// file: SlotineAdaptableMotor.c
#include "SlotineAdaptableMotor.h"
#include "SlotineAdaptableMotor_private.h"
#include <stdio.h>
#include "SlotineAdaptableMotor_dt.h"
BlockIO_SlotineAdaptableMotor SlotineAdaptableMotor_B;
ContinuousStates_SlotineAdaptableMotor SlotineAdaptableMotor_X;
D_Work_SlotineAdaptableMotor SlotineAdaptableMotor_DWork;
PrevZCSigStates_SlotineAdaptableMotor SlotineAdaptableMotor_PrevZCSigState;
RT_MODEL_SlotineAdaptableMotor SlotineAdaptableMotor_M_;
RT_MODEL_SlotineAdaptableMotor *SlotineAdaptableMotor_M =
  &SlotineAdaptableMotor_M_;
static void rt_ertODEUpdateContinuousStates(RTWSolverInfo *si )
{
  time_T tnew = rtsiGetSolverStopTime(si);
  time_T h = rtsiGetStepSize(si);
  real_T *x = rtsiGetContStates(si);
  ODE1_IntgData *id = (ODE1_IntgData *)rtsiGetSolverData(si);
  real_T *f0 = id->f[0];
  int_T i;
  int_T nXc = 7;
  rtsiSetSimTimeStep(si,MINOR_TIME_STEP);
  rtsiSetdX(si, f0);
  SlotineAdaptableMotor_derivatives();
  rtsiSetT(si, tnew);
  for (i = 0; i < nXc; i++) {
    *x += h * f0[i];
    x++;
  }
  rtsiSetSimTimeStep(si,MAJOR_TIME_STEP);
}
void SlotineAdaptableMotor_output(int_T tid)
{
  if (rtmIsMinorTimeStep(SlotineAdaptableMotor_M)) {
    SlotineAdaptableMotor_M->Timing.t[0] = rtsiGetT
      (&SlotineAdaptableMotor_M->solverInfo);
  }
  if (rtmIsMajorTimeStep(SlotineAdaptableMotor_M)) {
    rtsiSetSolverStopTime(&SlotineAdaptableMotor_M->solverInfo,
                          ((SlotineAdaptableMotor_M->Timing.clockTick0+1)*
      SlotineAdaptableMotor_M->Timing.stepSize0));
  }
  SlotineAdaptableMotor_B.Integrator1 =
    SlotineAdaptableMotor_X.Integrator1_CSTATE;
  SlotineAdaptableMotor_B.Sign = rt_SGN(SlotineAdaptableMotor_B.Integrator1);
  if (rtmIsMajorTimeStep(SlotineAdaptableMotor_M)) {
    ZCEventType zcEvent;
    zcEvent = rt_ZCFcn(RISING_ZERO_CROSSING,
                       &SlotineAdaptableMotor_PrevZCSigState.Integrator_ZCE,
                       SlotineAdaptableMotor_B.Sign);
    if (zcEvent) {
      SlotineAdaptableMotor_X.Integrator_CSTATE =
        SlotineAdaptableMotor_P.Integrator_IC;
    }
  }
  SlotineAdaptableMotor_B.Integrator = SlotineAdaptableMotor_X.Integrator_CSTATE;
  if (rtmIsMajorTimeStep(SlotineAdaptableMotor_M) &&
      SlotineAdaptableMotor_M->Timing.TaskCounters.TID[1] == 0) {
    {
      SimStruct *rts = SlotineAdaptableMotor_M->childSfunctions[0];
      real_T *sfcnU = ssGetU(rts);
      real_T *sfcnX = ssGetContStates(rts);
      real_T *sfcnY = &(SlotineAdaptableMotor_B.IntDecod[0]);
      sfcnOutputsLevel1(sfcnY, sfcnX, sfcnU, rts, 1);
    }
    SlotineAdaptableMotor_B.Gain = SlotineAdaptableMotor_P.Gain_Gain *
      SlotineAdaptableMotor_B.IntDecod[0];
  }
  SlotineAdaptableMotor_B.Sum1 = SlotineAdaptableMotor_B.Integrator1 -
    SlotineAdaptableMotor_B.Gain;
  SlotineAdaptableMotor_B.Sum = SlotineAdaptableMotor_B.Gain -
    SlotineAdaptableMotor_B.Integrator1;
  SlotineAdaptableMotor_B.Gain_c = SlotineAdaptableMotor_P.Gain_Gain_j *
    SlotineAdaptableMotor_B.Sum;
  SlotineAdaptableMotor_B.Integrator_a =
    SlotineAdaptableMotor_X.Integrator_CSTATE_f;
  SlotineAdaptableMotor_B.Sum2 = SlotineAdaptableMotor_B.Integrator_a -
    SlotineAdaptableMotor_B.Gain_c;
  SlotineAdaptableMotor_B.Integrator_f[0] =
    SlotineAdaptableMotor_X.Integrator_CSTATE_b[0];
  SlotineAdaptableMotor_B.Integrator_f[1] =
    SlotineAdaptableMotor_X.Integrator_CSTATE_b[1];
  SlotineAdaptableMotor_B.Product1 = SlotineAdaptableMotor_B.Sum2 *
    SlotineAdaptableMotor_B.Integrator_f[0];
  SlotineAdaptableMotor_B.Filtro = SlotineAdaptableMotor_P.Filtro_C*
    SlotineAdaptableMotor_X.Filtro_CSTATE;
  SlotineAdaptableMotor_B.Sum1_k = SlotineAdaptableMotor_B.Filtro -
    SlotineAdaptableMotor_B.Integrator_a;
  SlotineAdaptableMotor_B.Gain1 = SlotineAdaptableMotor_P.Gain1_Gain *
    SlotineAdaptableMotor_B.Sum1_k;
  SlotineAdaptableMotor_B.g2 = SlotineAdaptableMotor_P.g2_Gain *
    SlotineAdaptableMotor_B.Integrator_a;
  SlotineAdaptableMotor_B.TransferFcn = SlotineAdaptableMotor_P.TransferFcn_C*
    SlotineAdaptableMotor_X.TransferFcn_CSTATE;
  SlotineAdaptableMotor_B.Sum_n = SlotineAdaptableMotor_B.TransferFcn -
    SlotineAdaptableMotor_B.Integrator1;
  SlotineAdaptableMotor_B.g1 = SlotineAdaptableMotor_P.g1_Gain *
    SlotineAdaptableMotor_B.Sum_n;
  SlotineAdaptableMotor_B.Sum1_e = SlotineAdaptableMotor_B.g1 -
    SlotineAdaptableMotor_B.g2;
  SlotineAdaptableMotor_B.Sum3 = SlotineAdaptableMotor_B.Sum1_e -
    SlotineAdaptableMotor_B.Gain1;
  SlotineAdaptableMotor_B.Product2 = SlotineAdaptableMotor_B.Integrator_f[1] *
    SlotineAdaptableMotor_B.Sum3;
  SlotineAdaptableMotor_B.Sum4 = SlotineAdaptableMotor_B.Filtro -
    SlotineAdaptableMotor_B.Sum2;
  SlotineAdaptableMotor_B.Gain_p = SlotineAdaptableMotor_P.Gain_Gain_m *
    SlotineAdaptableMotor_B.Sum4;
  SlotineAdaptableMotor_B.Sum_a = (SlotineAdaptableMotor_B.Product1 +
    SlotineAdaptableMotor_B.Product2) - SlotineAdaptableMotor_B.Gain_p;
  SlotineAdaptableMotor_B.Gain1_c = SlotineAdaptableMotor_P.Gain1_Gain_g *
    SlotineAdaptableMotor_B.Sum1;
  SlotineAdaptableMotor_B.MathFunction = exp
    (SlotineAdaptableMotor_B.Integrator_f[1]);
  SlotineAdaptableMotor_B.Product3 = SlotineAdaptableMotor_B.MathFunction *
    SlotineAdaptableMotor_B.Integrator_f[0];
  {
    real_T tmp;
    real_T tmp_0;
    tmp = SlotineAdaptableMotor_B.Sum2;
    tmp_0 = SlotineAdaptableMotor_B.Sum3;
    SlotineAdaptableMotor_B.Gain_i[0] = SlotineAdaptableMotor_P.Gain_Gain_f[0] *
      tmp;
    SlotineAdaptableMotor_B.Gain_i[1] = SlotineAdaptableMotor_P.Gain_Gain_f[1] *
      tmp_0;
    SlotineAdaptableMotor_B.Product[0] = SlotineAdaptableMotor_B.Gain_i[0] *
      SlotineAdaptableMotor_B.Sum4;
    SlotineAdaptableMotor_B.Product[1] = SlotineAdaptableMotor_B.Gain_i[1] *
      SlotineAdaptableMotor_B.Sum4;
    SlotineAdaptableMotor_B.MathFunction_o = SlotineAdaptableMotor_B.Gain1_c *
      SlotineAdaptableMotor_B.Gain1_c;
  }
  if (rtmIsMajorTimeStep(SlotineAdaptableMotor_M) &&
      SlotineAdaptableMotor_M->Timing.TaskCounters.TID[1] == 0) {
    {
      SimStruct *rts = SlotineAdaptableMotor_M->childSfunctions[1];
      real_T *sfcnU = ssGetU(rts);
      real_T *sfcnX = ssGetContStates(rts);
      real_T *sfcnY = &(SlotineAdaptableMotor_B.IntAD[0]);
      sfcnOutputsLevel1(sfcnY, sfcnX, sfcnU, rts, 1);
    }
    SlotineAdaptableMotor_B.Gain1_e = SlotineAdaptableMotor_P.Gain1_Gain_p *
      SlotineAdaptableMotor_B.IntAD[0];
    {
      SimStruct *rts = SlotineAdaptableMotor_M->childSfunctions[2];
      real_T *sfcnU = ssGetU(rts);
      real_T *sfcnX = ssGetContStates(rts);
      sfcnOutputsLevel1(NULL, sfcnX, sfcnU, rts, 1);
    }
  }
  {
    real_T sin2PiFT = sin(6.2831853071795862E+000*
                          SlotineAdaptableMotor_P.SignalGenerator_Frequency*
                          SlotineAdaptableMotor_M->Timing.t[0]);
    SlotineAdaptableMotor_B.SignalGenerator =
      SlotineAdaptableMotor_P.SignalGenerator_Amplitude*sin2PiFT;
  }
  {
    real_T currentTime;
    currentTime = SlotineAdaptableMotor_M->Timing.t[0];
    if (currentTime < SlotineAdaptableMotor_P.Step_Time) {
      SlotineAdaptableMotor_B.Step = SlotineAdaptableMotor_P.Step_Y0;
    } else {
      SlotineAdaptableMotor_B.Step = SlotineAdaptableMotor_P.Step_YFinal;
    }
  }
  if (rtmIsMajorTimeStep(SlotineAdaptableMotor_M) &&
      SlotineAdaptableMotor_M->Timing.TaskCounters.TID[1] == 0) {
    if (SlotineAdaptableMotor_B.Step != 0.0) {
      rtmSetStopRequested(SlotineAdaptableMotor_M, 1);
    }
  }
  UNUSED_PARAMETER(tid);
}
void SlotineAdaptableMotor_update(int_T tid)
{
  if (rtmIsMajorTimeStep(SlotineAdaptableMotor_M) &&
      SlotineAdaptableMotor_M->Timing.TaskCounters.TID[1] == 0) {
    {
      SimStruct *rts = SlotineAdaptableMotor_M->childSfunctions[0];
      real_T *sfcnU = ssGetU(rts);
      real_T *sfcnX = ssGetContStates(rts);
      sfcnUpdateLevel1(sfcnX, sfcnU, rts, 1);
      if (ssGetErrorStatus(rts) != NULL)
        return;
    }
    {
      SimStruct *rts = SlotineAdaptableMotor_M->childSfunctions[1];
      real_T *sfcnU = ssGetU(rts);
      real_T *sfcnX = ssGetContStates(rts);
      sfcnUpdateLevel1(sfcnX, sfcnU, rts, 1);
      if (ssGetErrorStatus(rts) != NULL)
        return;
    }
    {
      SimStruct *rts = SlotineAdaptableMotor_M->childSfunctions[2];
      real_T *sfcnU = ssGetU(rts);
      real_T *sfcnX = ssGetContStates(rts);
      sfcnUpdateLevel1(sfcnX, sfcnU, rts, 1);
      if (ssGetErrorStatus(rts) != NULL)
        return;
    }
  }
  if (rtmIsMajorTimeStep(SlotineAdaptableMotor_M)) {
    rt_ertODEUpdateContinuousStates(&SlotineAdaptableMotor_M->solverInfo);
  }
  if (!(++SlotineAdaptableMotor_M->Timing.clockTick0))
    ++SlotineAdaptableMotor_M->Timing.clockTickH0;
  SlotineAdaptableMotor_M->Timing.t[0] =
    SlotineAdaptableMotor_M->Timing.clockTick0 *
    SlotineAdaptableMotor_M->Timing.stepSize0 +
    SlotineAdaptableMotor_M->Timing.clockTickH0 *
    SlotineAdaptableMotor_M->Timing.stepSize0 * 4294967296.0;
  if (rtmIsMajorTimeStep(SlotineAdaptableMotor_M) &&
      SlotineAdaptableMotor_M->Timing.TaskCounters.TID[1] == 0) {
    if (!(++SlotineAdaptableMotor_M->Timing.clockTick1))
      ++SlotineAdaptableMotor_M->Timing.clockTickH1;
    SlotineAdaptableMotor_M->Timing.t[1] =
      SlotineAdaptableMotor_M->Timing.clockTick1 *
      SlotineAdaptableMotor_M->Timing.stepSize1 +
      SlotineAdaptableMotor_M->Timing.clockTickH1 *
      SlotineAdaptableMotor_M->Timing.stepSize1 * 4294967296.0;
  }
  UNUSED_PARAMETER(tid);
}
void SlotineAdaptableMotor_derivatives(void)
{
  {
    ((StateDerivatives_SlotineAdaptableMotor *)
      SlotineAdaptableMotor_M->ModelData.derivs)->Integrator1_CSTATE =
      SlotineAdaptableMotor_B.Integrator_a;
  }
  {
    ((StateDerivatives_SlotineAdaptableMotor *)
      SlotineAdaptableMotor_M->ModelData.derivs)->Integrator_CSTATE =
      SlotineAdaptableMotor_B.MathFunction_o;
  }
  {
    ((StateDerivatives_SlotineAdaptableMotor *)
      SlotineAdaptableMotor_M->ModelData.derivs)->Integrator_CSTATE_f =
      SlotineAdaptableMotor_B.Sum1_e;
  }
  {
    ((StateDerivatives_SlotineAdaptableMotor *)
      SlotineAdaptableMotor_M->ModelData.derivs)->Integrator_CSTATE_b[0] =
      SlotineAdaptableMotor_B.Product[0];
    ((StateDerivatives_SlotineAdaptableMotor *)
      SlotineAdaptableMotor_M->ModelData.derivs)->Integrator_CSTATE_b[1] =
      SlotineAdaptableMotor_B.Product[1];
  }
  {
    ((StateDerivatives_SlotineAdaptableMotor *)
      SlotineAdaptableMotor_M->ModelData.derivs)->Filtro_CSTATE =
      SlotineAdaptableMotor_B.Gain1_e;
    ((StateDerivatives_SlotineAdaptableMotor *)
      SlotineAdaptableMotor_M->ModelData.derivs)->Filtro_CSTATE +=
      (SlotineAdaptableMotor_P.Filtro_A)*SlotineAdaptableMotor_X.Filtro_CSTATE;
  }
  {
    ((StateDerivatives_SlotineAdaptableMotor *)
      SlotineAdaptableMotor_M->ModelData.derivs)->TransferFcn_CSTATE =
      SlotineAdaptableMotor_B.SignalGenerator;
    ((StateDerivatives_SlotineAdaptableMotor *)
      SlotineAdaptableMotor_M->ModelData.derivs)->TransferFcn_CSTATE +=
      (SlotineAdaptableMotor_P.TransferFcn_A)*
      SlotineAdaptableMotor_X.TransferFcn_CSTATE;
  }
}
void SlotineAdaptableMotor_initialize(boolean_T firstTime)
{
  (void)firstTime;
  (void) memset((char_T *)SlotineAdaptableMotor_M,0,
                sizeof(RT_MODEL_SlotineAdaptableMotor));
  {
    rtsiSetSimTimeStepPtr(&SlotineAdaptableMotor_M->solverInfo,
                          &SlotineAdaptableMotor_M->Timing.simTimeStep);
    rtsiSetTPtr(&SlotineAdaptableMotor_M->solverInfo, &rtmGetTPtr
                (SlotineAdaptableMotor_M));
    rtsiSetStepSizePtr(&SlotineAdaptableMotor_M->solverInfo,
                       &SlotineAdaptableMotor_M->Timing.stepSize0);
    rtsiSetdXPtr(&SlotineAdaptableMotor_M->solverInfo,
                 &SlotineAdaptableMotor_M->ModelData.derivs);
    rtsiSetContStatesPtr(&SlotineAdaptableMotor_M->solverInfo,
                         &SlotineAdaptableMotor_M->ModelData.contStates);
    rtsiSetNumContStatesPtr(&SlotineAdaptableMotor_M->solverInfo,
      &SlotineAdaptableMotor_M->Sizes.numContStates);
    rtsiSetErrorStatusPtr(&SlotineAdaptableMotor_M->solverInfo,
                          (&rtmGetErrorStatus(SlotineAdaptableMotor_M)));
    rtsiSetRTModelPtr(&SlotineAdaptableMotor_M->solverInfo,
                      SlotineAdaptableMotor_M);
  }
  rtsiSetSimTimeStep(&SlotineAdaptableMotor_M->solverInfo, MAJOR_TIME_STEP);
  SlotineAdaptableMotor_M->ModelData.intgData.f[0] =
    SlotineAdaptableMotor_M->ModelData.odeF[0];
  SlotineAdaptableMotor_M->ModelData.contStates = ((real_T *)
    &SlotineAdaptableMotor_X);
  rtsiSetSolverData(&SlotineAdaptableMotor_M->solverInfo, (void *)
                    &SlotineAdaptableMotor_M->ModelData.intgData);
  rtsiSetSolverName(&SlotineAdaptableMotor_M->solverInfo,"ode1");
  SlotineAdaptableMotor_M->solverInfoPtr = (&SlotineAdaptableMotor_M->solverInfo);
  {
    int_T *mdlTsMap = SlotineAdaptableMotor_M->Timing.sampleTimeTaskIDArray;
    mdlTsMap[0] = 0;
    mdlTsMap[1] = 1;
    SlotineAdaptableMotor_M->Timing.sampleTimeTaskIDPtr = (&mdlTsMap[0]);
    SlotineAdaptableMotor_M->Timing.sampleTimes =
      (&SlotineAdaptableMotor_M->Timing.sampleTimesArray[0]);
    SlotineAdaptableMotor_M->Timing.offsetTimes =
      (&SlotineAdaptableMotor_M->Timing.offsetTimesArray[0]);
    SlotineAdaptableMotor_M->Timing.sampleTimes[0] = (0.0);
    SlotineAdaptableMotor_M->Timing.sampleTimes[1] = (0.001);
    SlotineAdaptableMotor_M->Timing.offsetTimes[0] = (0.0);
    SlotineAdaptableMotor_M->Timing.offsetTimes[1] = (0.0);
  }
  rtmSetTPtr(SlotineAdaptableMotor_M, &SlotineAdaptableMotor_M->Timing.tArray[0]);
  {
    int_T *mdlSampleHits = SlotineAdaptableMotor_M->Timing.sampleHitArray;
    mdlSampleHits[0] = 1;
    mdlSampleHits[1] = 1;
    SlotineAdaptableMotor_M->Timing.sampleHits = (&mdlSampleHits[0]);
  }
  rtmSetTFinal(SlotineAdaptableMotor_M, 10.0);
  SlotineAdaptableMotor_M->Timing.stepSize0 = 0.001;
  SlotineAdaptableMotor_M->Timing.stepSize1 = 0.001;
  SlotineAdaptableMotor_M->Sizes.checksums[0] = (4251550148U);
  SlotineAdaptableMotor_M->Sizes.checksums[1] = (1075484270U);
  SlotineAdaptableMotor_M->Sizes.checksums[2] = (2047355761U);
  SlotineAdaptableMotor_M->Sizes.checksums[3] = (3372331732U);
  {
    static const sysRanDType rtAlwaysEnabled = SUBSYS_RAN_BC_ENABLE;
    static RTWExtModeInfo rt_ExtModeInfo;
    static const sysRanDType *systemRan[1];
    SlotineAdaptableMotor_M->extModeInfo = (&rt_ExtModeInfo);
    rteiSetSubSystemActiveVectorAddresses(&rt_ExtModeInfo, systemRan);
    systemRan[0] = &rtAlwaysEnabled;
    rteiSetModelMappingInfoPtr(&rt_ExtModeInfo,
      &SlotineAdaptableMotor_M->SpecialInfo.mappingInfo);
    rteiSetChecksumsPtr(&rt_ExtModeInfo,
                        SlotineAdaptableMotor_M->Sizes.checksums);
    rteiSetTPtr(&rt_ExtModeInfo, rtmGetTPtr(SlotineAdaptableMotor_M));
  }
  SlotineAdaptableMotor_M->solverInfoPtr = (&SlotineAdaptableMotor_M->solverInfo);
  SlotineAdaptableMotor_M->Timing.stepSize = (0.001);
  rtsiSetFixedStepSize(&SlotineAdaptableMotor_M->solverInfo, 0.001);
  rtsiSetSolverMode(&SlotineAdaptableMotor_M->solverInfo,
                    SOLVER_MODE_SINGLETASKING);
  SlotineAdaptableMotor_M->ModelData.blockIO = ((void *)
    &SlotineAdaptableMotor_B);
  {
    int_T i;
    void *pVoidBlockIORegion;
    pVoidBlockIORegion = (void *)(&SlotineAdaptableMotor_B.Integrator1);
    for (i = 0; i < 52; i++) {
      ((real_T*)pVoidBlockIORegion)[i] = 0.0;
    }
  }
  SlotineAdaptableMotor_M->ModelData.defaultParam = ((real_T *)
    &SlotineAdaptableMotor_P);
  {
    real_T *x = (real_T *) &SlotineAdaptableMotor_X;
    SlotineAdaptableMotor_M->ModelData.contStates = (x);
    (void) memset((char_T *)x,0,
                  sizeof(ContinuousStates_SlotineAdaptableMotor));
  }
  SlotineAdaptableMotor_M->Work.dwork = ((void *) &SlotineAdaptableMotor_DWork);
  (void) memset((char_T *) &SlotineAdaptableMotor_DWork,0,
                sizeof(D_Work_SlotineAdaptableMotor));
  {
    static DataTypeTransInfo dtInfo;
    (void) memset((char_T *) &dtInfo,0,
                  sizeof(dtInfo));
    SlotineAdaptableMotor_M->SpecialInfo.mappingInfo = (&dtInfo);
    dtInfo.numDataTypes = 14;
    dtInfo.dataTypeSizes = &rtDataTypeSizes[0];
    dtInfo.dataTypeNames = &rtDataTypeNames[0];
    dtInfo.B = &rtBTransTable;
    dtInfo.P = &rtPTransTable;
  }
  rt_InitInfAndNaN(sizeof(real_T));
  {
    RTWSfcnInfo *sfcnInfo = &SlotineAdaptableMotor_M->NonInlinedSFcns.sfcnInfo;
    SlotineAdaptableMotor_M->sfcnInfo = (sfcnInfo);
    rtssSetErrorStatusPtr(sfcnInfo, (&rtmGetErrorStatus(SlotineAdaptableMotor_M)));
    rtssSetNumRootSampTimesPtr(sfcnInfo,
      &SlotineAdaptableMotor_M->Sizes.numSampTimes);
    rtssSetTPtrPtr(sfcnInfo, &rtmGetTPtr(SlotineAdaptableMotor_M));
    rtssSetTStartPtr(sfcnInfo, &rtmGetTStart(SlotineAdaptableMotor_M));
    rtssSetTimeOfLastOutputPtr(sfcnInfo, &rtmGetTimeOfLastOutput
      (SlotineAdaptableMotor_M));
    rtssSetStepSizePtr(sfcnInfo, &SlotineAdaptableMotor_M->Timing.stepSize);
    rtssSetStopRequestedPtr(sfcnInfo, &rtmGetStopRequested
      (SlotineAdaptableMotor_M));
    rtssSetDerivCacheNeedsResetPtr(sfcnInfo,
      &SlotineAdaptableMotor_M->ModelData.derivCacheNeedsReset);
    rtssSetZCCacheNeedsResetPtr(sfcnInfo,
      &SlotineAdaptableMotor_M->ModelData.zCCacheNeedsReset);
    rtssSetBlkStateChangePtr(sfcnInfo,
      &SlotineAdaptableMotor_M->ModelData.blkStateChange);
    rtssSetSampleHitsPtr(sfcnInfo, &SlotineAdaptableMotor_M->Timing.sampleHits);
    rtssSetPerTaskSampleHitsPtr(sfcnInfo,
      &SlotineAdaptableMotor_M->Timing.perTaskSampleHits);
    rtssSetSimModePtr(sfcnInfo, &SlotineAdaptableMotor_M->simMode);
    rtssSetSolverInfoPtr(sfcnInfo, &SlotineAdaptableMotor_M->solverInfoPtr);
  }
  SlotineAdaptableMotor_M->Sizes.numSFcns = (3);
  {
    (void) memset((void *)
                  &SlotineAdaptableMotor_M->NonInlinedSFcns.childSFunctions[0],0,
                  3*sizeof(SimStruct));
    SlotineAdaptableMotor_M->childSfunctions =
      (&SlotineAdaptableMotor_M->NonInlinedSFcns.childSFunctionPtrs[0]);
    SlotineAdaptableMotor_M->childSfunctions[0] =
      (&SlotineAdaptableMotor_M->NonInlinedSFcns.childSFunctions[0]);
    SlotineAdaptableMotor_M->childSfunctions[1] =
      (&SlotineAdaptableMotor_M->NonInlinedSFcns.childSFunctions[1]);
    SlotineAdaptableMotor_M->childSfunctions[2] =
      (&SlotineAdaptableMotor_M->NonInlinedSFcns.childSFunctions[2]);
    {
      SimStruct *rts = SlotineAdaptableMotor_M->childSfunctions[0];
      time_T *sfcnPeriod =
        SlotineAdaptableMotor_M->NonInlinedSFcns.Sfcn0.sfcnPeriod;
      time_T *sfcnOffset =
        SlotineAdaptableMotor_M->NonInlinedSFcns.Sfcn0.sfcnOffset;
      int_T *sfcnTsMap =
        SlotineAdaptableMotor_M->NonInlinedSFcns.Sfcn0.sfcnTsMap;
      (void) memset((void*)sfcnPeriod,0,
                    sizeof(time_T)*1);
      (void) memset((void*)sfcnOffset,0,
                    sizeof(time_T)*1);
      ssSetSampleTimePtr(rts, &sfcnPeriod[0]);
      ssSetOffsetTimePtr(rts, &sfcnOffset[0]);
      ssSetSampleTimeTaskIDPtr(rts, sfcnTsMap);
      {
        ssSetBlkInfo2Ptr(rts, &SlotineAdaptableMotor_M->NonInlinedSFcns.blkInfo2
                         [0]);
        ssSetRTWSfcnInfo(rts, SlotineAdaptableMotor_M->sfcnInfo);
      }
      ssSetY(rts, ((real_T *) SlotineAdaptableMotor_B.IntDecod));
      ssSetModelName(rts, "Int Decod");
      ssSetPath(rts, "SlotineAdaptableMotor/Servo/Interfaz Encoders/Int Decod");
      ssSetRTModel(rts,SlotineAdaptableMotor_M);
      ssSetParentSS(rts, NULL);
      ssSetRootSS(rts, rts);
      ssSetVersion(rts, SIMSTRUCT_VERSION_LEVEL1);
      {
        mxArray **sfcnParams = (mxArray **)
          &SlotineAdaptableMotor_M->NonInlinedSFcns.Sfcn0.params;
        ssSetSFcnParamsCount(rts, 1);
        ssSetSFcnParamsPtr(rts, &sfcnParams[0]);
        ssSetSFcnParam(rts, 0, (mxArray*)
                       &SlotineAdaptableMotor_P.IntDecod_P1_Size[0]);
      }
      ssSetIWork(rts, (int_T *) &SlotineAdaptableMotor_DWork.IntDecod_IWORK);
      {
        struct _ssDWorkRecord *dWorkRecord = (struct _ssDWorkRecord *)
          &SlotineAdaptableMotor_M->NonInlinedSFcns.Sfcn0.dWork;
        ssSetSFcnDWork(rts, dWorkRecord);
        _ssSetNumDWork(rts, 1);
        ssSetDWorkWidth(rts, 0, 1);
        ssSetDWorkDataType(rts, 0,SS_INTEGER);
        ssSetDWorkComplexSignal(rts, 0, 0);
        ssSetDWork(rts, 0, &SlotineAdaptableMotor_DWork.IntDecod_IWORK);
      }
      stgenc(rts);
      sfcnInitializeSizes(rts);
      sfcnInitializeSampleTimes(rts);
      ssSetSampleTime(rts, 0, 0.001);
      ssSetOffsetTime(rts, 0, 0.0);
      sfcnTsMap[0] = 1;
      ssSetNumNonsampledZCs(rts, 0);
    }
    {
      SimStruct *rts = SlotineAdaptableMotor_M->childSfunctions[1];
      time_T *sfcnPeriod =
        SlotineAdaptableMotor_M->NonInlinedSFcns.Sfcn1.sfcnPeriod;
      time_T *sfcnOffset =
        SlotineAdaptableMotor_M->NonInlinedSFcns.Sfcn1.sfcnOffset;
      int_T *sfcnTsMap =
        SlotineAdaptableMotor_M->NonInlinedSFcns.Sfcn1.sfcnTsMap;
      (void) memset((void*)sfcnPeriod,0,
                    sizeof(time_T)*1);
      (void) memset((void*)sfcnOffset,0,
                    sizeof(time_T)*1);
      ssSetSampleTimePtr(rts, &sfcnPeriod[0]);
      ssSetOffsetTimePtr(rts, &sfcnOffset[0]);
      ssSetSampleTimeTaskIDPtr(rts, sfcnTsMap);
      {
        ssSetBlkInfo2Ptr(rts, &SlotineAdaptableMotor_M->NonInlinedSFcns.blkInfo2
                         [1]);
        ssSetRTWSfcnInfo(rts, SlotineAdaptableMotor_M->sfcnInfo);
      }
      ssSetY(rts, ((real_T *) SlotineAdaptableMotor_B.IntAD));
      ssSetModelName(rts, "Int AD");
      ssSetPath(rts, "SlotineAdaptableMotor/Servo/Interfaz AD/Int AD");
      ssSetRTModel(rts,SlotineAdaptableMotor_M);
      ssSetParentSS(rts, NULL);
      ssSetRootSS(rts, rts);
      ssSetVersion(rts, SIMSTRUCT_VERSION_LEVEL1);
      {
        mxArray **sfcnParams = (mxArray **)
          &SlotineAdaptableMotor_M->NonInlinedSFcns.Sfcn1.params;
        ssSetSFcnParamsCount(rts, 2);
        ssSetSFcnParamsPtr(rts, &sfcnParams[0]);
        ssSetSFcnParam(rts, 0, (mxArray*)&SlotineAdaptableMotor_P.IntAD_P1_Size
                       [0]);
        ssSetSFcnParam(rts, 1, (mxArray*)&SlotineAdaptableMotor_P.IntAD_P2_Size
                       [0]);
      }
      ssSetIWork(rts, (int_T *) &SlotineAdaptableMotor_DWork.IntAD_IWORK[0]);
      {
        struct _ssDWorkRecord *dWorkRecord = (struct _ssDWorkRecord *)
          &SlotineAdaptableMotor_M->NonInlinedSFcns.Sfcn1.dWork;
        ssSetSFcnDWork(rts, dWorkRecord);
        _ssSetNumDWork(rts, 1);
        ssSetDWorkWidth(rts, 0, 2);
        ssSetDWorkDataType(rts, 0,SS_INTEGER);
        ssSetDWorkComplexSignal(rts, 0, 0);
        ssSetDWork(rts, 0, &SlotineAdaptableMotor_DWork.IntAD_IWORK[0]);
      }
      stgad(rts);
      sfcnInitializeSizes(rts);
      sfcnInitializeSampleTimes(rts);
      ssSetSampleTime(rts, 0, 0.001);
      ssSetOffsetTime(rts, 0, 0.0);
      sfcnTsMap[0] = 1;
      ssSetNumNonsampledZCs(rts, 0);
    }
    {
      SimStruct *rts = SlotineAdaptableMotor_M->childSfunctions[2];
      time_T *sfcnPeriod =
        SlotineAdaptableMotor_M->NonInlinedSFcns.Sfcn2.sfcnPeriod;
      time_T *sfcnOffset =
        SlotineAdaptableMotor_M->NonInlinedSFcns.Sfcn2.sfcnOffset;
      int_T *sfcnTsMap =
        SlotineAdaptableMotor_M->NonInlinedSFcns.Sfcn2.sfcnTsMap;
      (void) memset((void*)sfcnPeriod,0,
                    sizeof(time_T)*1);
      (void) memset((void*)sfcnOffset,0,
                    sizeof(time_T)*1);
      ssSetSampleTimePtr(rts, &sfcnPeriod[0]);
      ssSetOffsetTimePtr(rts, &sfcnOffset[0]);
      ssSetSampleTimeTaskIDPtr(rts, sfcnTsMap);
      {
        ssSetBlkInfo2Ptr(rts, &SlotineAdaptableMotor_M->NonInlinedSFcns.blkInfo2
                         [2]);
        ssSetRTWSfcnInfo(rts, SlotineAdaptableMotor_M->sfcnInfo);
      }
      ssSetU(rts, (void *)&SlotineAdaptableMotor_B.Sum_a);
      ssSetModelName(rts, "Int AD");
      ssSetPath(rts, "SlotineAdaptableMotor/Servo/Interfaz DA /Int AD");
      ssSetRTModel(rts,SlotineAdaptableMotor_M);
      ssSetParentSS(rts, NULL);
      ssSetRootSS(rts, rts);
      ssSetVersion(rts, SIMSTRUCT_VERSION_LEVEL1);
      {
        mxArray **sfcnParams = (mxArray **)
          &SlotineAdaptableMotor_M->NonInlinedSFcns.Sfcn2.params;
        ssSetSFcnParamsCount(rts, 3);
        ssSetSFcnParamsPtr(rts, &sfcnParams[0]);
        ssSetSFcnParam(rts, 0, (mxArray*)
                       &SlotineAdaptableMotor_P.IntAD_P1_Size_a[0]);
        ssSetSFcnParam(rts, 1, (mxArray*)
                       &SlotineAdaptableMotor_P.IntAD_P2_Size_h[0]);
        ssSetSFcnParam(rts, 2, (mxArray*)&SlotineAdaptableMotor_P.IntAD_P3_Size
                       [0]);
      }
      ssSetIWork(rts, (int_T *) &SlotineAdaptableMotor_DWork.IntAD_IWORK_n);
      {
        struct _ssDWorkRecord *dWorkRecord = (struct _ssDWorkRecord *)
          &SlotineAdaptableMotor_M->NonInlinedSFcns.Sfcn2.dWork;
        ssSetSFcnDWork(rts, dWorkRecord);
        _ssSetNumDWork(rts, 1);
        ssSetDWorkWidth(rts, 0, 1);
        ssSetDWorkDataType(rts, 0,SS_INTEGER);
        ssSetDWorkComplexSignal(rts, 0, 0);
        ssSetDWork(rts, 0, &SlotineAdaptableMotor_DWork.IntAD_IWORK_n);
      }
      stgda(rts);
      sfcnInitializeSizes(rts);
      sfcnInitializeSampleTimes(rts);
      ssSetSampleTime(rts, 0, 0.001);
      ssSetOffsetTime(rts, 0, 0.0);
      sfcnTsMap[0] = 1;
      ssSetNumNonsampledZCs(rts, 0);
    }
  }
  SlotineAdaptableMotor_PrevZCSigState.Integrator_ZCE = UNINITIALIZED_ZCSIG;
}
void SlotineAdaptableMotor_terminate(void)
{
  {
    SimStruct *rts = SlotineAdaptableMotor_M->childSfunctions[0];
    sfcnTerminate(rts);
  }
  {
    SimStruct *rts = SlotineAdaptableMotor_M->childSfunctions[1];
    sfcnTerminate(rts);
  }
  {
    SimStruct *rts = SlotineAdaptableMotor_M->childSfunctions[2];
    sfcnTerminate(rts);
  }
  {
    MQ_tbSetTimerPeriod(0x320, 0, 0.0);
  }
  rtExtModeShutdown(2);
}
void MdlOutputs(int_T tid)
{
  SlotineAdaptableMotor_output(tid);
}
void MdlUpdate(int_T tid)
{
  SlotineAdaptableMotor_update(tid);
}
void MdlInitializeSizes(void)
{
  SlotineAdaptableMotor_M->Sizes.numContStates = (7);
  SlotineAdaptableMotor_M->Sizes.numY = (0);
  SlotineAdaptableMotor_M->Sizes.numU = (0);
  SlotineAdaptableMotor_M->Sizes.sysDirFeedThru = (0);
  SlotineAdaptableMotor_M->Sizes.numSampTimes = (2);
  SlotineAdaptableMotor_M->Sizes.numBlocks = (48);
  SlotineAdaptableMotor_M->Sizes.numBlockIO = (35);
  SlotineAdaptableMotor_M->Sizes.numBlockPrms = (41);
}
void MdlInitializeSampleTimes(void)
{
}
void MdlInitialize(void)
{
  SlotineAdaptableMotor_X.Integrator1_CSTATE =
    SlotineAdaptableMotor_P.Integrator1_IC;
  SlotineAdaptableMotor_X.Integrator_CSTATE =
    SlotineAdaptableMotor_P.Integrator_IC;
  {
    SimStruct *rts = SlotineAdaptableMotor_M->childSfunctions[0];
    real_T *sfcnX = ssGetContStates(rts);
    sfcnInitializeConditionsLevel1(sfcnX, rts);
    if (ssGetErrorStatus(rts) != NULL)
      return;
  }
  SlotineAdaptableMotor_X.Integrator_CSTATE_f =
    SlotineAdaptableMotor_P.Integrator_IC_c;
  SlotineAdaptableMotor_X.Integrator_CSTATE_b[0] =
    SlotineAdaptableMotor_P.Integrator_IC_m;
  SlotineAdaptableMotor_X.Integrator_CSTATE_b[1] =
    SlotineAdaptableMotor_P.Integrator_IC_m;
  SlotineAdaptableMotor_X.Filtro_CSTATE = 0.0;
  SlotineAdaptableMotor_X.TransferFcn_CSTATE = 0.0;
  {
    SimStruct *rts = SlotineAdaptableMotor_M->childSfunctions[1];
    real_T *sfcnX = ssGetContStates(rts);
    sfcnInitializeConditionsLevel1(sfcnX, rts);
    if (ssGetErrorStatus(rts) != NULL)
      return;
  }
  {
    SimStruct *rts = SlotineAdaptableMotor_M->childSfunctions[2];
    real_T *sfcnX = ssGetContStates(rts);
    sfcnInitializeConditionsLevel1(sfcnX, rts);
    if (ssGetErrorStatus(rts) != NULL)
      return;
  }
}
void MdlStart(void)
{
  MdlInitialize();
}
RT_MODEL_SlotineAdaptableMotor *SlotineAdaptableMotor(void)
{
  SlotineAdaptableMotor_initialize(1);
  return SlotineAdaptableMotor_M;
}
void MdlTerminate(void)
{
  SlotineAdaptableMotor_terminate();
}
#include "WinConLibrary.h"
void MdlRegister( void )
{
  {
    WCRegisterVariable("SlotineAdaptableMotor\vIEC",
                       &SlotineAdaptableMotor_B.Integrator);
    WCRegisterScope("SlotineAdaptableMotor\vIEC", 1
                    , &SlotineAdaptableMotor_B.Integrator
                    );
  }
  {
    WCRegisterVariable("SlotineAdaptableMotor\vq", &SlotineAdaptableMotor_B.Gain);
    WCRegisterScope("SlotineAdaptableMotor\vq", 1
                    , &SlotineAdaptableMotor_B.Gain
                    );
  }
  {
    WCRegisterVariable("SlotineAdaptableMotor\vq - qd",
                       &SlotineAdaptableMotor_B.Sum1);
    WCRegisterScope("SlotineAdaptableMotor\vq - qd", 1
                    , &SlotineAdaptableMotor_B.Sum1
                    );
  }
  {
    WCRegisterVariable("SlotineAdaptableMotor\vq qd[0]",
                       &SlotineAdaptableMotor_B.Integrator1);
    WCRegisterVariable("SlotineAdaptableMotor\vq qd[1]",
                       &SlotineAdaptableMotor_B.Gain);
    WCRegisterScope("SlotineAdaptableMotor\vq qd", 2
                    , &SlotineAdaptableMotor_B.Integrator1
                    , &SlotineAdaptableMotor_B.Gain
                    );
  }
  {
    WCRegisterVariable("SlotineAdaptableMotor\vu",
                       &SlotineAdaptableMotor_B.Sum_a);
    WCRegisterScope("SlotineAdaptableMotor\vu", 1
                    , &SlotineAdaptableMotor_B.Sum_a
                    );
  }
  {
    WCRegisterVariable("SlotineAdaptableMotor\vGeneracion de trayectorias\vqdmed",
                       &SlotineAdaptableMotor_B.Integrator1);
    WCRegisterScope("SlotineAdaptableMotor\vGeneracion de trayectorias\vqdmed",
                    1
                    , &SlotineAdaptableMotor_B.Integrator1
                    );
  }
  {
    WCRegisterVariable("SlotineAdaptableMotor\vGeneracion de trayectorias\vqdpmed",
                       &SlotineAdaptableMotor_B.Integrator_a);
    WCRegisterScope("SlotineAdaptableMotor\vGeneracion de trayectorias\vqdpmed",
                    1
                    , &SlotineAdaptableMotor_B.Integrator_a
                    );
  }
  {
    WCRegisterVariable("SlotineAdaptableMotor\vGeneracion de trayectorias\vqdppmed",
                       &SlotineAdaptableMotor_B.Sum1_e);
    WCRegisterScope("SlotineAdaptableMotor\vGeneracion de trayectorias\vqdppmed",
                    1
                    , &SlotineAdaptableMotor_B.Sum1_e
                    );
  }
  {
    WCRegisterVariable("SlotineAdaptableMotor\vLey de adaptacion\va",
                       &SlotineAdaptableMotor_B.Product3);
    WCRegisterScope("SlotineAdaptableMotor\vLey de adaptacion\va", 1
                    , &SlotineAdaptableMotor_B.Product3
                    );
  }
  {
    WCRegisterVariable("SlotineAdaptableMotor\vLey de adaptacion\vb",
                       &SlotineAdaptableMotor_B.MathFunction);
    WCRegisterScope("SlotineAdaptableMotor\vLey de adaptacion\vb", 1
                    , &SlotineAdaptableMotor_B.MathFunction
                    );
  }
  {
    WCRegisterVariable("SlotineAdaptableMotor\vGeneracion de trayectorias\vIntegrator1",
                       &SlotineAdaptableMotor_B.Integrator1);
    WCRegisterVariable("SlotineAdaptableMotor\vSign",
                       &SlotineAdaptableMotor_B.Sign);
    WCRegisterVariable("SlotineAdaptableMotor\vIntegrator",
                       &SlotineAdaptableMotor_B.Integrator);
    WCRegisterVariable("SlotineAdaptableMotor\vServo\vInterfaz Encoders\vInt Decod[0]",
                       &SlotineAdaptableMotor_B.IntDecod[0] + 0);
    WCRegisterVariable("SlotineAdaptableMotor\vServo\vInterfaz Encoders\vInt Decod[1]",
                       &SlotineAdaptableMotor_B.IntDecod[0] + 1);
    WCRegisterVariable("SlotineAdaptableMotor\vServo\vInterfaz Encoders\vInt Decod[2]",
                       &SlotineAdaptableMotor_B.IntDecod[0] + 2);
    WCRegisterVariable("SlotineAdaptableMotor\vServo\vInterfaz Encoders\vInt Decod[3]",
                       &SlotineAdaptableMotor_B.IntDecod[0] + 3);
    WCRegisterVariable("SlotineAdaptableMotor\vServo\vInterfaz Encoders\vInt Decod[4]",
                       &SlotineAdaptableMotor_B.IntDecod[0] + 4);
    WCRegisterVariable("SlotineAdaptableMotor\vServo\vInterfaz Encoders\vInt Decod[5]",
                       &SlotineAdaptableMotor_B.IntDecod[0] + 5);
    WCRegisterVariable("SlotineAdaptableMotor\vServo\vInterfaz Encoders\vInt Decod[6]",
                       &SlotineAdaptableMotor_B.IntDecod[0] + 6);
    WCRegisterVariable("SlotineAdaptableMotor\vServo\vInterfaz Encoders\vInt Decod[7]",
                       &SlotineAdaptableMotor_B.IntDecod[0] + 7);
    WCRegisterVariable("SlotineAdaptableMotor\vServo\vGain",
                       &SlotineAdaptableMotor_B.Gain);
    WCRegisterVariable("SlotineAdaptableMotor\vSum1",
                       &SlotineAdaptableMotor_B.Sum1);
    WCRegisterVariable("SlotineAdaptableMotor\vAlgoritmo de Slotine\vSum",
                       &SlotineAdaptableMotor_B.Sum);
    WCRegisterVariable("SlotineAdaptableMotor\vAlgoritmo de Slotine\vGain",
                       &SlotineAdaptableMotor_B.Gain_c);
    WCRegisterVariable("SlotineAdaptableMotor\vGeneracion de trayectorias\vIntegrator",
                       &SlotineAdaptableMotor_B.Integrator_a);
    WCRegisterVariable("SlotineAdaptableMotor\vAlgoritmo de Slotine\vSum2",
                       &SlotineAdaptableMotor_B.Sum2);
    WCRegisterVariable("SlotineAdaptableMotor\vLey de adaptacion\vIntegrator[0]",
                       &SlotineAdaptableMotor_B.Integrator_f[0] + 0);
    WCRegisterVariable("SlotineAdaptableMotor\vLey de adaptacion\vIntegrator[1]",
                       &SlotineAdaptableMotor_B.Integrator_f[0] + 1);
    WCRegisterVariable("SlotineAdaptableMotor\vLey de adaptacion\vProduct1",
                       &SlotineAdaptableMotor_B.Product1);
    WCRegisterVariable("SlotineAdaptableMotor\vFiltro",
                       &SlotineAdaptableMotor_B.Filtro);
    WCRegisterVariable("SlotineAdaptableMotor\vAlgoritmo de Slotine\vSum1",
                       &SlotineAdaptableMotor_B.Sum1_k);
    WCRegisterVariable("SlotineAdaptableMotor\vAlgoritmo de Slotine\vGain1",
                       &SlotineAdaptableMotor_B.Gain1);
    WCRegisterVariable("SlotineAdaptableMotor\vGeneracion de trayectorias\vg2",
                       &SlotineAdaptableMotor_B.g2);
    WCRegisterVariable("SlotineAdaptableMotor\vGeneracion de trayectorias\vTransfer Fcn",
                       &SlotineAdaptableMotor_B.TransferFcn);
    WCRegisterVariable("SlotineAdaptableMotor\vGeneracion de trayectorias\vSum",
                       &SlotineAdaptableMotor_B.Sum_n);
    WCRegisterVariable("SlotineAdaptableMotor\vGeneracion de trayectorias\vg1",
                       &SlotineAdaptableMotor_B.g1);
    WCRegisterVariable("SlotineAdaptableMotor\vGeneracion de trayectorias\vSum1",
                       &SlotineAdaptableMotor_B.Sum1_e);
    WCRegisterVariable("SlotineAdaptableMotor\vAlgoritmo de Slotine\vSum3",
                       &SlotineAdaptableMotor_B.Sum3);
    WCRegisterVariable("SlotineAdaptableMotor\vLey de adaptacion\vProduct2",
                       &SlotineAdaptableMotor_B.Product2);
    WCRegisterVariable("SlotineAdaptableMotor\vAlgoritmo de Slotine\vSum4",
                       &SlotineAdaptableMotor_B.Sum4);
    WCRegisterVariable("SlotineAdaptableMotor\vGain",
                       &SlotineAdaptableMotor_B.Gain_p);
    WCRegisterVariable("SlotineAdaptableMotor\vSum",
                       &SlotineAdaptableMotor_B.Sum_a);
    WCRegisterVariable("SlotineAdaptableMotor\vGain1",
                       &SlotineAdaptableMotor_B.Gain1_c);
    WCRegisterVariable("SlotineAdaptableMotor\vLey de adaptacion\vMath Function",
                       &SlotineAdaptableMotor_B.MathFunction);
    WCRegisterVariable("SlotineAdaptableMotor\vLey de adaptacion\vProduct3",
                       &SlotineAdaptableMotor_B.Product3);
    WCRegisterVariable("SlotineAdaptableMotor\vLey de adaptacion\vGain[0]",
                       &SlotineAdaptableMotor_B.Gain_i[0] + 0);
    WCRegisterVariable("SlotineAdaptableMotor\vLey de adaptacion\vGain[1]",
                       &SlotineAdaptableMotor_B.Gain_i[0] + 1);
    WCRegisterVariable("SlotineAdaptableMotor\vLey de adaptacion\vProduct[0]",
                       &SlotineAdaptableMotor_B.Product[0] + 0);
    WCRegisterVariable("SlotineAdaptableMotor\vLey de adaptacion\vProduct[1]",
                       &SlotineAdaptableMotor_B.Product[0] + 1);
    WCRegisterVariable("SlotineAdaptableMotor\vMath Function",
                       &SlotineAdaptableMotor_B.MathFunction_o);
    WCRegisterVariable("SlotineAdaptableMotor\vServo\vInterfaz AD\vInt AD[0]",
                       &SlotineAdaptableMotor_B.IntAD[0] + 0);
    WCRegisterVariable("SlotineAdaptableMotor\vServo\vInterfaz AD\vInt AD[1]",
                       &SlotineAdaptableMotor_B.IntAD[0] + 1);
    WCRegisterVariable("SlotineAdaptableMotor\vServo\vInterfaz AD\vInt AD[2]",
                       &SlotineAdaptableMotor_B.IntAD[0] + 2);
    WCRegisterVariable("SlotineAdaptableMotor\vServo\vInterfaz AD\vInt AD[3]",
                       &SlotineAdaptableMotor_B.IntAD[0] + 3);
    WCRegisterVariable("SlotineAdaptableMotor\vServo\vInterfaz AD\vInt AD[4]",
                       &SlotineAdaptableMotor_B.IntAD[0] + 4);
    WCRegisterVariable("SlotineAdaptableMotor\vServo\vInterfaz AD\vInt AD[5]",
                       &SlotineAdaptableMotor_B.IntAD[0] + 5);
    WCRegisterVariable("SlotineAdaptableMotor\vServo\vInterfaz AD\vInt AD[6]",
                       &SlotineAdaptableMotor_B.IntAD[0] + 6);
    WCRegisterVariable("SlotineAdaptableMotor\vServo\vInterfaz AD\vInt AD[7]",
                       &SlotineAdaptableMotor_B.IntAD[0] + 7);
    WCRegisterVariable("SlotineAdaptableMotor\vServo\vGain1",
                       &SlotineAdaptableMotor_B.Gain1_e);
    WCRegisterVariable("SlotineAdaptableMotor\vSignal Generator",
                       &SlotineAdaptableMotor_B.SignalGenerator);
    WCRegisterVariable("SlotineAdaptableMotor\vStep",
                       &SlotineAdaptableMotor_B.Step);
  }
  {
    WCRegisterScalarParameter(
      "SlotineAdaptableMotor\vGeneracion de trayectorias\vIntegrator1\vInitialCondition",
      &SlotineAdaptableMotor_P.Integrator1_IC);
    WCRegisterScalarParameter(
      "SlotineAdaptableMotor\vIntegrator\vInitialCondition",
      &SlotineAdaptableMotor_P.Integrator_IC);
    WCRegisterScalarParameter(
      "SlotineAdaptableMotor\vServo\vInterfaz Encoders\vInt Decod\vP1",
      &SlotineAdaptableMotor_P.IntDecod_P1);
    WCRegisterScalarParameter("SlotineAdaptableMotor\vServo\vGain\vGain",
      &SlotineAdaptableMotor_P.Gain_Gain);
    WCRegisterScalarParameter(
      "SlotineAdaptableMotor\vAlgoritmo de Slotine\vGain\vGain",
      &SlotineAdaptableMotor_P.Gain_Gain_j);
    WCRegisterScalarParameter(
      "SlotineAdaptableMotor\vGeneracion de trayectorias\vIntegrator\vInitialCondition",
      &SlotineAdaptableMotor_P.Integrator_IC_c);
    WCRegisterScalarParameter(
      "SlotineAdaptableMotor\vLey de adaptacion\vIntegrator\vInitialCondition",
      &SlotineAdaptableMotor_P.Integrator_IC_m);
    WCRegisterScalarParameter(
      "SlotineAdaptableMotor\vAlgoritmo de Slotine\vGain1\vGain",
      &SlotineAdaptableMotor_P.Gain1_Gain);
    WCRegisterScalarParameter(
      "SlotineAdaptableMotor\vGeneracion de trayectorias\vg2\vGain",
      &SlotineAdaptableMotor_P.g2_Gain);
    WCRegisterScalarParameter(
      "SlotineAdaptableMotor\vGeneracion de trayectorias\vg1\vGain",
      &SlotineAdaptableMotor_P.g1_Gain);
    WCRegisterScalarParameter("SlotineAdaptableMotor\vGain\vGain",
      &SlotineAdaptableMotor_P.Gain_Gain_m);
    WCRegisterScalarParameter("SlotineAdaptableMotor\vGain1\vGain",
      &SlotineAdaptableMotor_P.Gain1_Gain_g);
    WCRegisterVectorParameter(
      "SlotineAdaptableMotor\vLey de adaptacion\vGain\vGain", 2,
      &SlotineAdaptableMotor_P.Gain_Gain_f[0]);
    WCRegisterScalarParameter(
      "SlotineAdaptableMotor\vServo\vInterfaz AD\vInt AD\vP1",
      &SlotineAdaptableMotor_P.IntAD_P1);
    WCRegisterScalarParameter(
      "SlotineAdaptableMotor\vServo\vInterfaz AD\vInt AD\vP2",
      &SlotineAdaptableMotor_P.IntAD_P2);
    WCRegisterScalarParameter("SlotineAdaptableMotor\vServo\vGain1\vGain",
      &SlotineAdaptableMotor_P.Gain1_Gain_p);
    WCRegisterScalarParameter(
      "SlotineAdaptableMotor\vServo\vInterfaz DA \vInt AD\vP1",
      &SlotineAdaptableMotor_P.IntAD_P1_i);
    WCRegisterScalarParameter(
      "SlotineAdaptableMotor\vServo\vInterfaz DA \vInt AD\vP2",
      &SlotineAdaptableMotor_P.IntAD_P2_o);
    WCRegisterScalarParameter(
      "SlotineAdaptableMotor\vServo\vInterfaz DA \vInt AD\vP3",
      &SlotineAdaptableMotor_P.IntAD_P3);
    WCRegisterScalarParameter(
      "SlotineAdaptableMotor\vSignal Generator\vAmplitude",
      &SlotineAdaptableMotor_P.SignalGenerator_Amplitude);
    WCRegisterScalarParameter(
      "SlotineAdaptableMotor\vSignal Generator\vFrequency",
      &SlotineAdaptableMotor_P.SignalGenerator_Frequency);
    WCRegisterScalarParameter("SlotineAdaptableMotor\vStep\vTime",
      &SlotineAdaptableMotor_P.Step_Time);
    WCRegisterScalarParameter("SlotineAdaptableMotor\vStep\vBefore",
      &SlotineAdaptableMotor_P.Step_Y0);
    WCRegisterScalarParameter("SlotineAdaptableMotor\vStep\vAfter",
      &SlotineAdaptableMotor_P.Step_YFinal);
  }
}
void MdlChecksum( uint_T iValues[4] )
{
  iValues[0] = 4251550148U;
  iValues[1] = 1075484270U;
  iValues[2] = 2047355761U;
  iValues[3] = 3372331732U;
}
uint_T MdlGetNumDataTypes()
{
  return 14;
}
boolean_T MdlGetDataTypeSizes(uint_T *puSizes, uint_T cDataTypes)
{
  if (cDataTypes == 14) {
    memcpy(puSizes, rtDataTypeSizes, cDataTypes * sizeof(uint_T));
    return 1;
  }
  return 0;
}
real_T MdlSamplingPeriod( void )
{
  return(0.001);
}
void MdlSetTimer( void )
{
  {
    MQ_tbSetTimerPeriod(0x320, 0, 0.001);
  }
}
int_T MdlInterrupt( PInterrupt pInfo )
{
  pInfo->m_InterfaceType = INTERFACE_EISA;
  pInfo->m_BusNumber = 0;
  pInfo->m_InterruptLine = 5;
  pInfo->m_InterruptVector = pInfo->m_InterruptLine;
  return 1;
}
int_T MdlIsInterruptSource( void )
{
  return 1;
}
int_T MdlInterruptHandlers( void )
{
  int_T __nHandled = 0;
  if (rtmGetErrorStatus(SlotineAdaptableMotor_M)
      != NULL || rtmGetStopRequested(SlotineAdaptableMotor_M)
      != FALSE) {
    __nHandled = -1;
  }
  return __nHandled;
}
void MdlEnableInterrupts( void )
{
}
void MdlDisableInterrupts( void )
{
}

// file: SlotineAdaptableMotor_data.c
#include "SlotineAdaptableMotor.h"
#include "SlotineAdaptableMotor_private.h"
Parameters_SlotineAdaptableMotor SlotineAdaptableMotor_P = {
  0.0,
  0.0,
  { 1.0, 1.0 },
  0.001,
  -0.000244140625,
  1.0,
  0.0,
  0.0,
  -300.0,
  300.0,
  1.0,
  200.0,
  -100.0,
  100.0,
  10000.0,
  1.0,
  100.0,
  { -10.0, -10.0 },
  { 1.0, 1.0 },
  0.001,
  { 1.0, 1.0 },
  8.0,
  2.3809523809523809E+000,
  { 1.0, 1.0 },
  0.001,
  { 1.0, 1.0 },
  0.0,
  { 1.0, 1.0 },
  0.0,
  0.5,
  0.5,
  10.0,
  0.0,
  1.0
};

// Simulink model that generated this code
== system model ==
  Integrator : Integrator  ExternalReset=rising  <- 1: MathFunction, 2: Sign
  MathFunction : Math  Operator=square  <- 1: Gain1
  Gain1 : Gain  Gain=100  <- 1: Sum1
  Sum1 : Sum  Inputs=+-  <- 1: Integrator1, 2: Servo
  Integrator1 : Integrator  <- 1: Integrator#1
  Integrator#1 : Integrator  <- 1: Sum#1
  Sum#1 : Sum  Inputs=-+  <- 1: g2, 2: g1
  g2 : Gain  Gain=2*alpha  <- 1: Integrator#1
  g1 : Gain  Gain=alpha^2  <- 1: Sum
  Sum : Sum  Inputs=-+  <- 1: Integrator1, 2: TransferFcn
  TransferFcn : TransferFcn  Numerator=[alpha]  Denominator=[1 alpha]  <- 1: SignalGenerator
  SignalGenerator : SignalGenerator  Amplitude=0.5  Frequency=0.5
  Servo : Plantilla_Servo_2014/Servo  <- 1: Sum#2
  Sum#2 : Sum  Inputs=++-  <- 1: Product1, 2: Product2, 3: Gain
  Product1 : Product  <- 1: Sum2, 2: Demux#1
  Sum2 : Sum  Inputs=-+  <- 1: Gain#1, 2: Integrator#1
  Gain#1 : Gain  Gain=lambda  <- 1: Sum#3
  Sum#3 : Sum  Inputs=-+  <- 1: Integrator1, 2: Servo
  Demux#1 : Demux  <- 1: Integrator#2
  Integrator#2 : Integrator  <- 1: Product
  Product : Product  <- 1: Gain#2, 2: Sum4
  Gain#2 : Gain  Gain=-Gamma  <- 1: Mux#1
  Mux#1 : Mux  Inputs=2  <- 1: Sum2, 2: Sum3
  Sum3 : Sum  Inputs=-+  <- 1: Gain#3, 2: Sum#1
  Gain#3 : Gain  Gain=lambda  <- 1: Sum#4
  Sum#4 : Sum  Inputs=-+  <- 1: Integrator#1, 2: Filtro
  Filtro : TransferFcn  Numerator=[300]  Denominator=[1 300]  <- 1: Servo/2
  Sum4 : Sum  Inputs=-+  <- 1: Sum2, 2: Filtro
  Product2 : Product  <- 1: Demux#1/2, 2: Sum3
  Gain : Gain  Gain=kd  <- 1: Sum4
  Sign : Signum  <- 1: Integrator1
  Product3 : Product  <- 1: Math#1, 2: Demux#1
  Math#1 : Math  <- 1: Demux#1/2
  Stop#1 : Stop  <- 1: Step
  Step : Step  Time=10
